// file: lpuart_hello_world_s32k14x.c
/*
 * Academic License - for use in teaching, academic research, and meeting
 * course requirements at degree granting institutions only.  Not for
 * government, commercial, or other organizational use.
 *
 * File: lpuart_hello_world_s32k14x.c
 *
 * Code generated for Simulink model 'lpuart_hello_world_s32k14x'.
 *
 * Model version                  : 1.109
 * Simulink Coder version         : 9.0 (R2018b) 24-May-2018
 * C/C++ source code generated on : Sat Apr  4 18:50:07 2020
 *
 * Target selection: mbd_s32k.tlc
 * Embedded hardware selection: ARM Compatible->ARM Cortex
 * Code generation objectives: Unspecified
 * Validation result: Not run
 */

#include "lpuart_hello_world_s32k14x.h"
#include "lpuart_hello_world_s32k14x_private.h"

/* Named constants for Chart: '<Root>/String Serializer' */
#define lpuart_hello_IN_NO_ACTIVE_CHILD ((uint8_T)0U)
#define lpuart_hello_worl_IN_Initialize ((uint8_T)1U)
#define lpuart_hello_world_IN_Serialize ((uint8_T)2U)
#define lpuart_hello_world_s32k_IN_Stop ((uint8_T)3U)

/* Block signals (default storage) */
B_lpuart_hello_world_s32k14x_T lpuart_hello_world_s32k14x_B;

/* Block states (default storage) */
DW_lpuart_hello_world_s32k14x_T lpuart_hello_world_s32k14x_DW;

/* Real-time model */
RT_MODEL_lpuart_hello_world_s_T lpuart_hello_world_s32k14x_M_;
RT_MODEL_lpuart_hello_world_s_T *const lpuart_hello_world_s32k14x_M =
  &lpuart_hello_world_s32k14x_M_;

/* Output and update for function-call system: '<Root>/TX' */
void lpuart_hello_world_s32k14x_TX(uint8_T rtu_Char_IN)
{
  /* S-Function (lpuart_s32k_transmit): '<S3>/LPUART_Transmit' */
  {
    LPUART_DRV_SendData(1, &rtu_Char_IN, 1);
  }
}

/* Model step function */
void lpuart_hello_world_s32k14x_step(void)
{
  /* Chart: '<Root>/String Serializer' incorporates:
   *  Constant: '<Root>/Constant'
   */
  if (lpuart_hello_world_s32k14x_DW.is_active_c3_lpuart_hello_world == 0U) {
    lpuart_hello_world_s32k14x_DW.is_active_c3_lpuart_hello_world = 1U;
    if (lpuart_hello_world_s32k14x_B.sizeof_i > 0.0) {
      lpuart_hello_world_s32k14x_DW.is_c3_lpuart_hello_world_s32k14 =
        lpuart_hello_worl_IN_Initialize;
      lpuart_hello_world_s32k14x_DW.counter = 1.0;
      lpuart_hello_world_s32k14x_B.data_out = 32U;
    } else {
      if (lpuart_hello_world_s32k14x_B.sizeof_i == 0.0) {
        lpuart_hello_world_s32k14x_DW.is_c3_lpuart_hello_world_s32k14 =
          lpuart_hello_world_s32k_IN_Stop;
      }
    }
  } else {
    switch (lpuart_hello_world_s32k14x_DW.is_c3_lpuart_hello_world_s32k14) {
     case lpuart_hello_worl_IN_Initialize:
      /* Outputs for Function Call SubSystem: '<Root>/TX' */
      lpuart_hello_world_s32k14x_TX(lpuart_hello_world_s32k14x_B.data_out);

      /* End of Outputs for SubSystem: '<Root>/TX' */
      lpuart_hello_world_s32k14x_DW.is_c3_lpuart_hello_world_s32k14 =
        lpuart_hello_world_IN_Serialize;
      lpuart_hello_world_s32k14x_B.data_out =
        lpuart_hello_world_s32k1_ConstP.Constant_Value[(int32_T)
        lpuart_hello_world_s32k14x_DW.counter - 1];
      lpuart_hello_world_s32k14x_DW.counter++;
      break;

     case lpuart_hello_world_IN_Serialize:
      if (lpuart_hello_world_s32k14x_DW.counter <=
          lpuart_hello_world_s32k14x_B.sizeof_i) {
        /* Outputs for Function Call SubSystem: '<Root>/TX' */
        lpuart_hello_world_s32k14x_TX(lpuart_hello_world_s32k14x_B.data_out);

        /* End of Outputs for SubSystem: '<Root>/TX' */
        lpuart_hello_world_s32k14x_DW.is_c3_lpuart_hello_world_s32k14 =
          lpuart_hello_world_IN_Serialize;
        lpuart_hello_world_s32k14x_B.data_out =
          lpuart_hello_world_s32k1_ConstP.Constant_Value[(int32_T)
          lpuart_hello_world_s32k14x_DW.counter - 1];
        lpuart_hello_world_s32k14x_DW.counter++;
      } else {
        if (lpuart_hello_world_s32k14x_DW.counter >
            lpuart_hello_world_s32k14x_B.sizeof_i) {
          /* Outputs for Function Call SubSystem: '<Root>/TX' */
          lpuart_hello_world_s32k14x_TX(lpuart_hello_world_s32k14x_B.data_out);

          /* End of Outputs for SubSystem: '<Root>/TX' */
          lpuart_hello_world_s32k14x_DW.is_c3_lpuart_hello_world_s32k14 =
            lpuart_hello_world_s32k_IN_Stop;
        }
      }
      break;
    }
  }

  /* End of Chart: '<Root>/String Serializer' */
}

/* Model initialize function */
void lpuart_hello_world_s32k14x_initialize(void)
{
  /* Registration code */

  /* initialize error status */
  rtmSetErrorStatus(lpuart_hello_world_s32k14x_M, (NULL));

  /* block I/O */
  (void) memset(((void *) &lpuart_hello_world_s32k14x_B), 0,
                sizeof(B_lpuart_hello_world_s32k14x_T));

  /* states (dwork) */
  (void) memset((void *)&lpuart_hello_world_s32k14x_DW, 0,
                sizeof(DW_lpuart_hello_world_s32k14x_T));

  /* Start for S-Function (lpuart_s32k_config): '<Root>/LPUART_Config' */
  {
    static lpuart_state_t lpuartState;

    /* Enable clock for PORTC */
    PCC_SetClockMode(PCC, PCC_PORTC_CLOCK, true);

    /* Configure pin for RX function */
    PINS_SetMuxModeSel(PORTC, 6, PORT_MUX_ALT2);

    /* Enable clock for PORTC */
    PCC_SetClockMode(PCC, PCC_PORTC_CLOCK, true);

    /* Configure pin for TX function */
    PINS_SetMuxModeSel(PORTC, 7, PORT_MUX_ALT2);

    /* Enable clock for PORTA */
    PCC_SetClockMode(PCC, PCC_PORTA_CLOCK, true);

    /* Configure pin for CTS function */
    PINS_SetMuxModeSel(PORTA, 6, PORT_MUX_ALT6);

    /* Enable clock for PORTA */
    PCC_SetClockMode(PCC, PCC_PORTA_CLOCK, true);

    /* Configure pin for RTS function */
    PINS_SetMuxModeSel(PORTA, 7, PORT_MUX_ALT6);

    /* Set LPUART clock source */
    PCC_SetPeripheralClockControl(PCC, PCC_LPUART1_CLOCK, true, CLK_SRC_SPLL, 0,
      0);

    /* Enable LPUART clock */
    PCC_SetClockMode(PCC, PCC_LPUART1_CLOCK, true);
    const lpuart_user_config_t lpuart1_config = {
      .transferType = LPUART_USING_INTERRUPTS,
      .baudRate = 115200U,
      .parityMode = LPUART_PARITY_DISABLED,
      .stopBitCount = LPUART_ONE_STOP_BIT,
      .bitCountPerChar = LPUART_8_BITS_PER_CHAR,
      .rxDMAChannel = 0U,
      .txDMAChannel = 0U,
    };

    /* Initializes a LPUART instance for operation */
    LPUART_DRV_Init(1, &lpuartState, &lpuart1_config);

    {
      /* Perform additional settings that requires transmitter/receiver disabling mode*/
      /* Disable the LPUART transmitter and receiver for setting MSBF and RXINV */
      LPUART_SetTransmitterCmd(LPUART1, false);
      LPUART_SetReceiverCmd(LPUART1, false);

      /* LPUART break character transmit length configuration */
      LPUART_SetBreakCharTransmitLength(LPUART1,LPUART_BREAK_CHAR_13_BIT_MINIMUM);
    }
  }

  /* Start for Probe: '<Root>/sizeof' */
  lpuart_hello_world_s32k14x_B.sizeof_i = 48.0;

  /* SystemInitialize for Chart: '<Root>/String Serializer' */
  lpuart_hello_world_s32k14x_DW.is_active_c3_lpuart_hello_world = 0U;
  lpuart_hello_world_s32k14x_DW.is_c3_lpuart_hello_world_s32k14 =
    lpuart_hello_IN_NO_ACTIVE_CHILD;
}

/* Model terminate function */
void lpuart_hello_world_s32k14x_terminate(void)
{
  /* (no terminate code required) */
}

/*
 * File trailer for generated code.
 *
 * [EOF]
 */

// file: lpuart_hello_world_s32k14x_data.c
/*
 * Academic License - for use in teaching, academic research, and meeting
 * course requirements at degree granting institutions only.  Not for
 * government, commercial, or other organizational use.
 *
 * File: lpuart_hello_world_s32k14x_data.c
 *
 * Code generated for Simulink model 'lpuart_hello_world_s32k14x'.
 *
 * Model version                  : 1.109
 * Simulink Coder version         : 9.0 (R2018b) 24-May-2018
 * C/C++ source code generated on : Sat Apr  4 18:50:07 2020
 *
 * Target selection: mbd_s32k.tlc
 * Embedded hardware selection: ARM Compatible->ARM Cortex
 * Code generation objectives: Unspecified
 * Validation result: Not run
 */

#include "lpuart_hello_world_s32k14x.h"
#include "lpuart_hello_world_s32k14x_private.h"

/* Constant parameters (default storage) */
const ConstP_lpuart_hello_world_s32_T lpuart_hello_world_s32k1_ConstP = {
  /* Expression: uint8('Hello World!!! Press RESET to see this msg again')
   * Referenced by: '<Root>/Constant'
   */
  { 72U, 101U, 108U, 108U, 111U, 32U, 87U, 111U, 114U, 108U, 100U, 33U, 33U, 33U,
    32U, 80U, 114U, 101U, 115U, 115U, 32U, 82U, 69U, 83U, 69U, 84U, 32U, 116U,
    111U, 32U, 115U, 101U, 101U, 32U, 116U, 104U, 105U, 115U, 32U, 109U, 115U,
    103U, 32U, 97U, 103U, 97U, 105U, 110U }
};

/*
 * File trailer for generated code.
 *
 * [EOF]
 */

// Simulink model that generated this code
simulink model "lpuart_hello_world_s32k14x"  (Simulink 9.2)
settings: Solver=FixedStepDiscrete  StartTime=0.0  StopTime=10.0  FixedStep=0.1  RelTol=1e-3  EnableMultiTasking=on
InitFcn:
  | mbd_s32k_consistency_checks(bdroot(gcs));
undefined symbols (not defined in the file): LQFP
libraries: mbd_s32k1xx_ec_toolbox x3, simulink x1

== system lpuart_hello_world_s32k14x ==
  Constant : Constant  Value=uint8('Hello World!!! Press RESET to see this msg again')  SampleTime=-1
  LPUART_Config : mbd_s32k1xx_ec_toolbox/Communication Blocks/UART Blocks/LPUART_Config  Priority=1  instance=1  baudrate=115200  databits=8  parity=None  sbns=1  bothedge=rising edge  rxinv=off  txinv=off  show_adv_opts=on  brk13=13 - 16 bit times  lbkde=13 - 16 bit times  rx=PTC6: [LPUART1_RX | Receive]  tx=PTC7: [LPUART1_TX | Transmit]  cts=PTA6: [LPUART1_CTS | Clear To Send (bar)]  rts=PTA7: [LPUART1_RTS | Request To Send]
  MBD_S32K14x_Config_Information : mbd_s32k1xx_ec_toolbox/MBD_S32K1xx_Config_Information  Priority=0  mbdt_ver=0  disp_str=|  config_params=[]  mcu_target_name=S32K144  mcu_target_package=100-LQFP  mcu_target_sram_size=64KB  mcu_system_clock_freq=80  mcu_xtal_freq=External 8  mcu_steptick_timer=LPIT Channel 0  mcu_steptick_prio=15  ds_import_enable=on  target_compiler=GCC  target_memory=FLASH  gcc_target_compile_opts=-mcpu=cortex-m4 -mthumb -mfloat-abi=hard -mfpu=fpv4-sp-d16 -O1 -g -gstrict-dwarf  gcc_target_assemble_opts=-mcpu=cortex-m4 -mthumb -mfloat-abi=hard -mfpu=fpv4-sp-d16 -g  gcc_target_link_opts=-mcpu=cortex-m4 -mthumb -mfloat-abi=hard -mfpu=fpv4-sp-d16  gcc_target_default_lcf=on  gcc_target_user_lcf=S32K144_64_flash.ld  ghs_target_compile_opts=-cpu=cortexm4f -thumb -DARM_MATH_CM4 -fpu=vfpv4_d16 -fsingle -Ogeneral -Wundef -Wimplicit-int -Wshadow -Wtrigraphs --no_commons --gnu_asm -gnu99 -gdwarf-2 -G  ghs_target_assemble_opts=-cpu=cortexm4f -fpu=vfpv4_d16  ghs_target_link_opts=-cpu=cortexm4f -thumb -fpu=vfpv4_d16  ghs_target_default_lcf=off  ghs_target_user_lcf=S32K144_64_flash.ld  iar_target_compile_opts=--cpu=Cortex-M4F --thumb --fpu=VFPv4_sp -Ol -e --debug --dlib_config normal  iar_target_assemble_opts=--cpu Cortex-M4F --thumb --fpu VFPv4_sp  iar_target_link_opts=--no_exceptions --vfe --inline  iar_target_default_lcf=off  iar_target_user_lcf=S32K144_64_flash.icf  pil_download_enable=off  rbl_download_enable=on  rbl_start_delay=5000000  rbl_download_interface=OpenSDA  rbl_restart_request=off  rbl_com_port=Custom  rbl_com_port_custom=COM1  pil_download_rate=57600  pil_opensda_drive=D: EVB-S32K144  pil_opensda_drive_custom=D  pil_uart_instance=1  pil_uart_rx=PTC6: [LPUART1_RX | Receive]  pil_uart_tx=PTC7: [LPUART1_TX | Transmit]  FTM_PWM_PcrCheckEnDis=on  FTM_Input_Edge_Inputs_PcrCheckEnDis=on  FTM_Dual_Edge_Inputs_PcrCheckEnDis=on  FTM_Quadrature_Inputs_PcrCheckEnDis=on  FTM_Hall_Sensor_Inputs_PcrCheckEnDis=on  LPTMR_PcrCheckEnDis=on  PIT_PcrCheckEnDis=on  RTC_PcrCheckEnDis=on  FlexCAN_PcrCheckEnDis=on  LIN_PcrCheckEnDis=on  FlexIO_PcrCheckEnDis=on  LPI2C_PcrCheckEnDis=on  LPSPI_PcrCheckEnDis=on  LPUART_PcrCheckEnDis=on  CMP_PcrCheckEnDis=on  GPIO_OutputPcrCheckEnDis=on  GPIO_InputPcrCheckEnDis=on  SBC_PcrCheckEnDis=on  AMMCLIB_PcrCheckEnDis=on  FM_PcrCheckEnDis=on  Profile_PcrCheckEnDis=on  ConfigParams_PcrCheckEnDis=on  ModelRef_PcrCheckEnDis=on  PDB0_PcrCheckEnDis=on  CSEc_PcrCheckEnDis=on  eDMA_PcrCheckEnDis=on  ADC_PcrCheckEnDis=on  WDOG_PcrCheckEnDis=on
      | Target : S32K144-64KB_SRAM
      | Package : 100-pin
      | System clock : 80 MHz
      | XTAL clock : External 8 MHz
      | Compiler : GCC
      | Target Type : FLASH
      | Download Code after build : (OpenSDA: E)
      | Step Tick Interrupt Priority : 15
  Model Info : simulink/Model-Wide Utilities/Model Info  Frame=off  DisplayStringWithTags=|  HorizontalTextAlignment=Left  LeftAlignmentValue=0.02
      | Model Name: %<ModelName>
      | 
      | Description: %<Description>
  String Serializer : Stateflow chart  TreatAsAtomicUnit=on
  TX : Subsystem  TreatAsAtomicUnit=on
  sizeof : Probe  ProbeSampleTime=off  ProbeComplexSignal=off
  wires:
  sizeof/1 -> String Serializer/2(data_length)
  Constant/1 -> sizeof/1, String Serializer/1(data_string)
  String Serializer/2(trigger_tx()) -> TX/Trigger
  String Serializer/1(data_out) -> TX/1(Char_IN)

== system lpuart_hello_world_s32k14x/TX ==
  Char_IN : Inport
  function : TriggerPort  TriggerType=function-call  VariantControl=Variant
  LPUART_Transmit : mbd_s32k1xx_ec_toolbox/Communication Blocks/UART Blocks/LPUART_Transmit  Priority=2  instance=1
  wires:
  Char_IN/1 -> LPUART_Transmit/1

== stateflow chart String Serializer ==
  state Initialize
    entry:
    counter = 1;
    data_out = uint8(32);
  state Serialize
    entry:
    data_out = uint8(data_string(counter));
    counter = counter+1;
  state Stop
  (default) -> Initialize [order 1] : [data_length > 0]
  Initialize -> Serialize : {trigger_tx}
  Serialize -> Serialize [order 1] : [counter <= data_length]
      | {trigger_tx;}
  Serialize -> Stop [order 2] : [counter > data_length]
      | {trigger_tx}
  (default) -> Stop [order 2] : [data_length == 0]
  data: data_string input double; data_length input double; data_out output uint8; counter local double
  events: trigger_tx output FUNCTION_CALL_EVENT
